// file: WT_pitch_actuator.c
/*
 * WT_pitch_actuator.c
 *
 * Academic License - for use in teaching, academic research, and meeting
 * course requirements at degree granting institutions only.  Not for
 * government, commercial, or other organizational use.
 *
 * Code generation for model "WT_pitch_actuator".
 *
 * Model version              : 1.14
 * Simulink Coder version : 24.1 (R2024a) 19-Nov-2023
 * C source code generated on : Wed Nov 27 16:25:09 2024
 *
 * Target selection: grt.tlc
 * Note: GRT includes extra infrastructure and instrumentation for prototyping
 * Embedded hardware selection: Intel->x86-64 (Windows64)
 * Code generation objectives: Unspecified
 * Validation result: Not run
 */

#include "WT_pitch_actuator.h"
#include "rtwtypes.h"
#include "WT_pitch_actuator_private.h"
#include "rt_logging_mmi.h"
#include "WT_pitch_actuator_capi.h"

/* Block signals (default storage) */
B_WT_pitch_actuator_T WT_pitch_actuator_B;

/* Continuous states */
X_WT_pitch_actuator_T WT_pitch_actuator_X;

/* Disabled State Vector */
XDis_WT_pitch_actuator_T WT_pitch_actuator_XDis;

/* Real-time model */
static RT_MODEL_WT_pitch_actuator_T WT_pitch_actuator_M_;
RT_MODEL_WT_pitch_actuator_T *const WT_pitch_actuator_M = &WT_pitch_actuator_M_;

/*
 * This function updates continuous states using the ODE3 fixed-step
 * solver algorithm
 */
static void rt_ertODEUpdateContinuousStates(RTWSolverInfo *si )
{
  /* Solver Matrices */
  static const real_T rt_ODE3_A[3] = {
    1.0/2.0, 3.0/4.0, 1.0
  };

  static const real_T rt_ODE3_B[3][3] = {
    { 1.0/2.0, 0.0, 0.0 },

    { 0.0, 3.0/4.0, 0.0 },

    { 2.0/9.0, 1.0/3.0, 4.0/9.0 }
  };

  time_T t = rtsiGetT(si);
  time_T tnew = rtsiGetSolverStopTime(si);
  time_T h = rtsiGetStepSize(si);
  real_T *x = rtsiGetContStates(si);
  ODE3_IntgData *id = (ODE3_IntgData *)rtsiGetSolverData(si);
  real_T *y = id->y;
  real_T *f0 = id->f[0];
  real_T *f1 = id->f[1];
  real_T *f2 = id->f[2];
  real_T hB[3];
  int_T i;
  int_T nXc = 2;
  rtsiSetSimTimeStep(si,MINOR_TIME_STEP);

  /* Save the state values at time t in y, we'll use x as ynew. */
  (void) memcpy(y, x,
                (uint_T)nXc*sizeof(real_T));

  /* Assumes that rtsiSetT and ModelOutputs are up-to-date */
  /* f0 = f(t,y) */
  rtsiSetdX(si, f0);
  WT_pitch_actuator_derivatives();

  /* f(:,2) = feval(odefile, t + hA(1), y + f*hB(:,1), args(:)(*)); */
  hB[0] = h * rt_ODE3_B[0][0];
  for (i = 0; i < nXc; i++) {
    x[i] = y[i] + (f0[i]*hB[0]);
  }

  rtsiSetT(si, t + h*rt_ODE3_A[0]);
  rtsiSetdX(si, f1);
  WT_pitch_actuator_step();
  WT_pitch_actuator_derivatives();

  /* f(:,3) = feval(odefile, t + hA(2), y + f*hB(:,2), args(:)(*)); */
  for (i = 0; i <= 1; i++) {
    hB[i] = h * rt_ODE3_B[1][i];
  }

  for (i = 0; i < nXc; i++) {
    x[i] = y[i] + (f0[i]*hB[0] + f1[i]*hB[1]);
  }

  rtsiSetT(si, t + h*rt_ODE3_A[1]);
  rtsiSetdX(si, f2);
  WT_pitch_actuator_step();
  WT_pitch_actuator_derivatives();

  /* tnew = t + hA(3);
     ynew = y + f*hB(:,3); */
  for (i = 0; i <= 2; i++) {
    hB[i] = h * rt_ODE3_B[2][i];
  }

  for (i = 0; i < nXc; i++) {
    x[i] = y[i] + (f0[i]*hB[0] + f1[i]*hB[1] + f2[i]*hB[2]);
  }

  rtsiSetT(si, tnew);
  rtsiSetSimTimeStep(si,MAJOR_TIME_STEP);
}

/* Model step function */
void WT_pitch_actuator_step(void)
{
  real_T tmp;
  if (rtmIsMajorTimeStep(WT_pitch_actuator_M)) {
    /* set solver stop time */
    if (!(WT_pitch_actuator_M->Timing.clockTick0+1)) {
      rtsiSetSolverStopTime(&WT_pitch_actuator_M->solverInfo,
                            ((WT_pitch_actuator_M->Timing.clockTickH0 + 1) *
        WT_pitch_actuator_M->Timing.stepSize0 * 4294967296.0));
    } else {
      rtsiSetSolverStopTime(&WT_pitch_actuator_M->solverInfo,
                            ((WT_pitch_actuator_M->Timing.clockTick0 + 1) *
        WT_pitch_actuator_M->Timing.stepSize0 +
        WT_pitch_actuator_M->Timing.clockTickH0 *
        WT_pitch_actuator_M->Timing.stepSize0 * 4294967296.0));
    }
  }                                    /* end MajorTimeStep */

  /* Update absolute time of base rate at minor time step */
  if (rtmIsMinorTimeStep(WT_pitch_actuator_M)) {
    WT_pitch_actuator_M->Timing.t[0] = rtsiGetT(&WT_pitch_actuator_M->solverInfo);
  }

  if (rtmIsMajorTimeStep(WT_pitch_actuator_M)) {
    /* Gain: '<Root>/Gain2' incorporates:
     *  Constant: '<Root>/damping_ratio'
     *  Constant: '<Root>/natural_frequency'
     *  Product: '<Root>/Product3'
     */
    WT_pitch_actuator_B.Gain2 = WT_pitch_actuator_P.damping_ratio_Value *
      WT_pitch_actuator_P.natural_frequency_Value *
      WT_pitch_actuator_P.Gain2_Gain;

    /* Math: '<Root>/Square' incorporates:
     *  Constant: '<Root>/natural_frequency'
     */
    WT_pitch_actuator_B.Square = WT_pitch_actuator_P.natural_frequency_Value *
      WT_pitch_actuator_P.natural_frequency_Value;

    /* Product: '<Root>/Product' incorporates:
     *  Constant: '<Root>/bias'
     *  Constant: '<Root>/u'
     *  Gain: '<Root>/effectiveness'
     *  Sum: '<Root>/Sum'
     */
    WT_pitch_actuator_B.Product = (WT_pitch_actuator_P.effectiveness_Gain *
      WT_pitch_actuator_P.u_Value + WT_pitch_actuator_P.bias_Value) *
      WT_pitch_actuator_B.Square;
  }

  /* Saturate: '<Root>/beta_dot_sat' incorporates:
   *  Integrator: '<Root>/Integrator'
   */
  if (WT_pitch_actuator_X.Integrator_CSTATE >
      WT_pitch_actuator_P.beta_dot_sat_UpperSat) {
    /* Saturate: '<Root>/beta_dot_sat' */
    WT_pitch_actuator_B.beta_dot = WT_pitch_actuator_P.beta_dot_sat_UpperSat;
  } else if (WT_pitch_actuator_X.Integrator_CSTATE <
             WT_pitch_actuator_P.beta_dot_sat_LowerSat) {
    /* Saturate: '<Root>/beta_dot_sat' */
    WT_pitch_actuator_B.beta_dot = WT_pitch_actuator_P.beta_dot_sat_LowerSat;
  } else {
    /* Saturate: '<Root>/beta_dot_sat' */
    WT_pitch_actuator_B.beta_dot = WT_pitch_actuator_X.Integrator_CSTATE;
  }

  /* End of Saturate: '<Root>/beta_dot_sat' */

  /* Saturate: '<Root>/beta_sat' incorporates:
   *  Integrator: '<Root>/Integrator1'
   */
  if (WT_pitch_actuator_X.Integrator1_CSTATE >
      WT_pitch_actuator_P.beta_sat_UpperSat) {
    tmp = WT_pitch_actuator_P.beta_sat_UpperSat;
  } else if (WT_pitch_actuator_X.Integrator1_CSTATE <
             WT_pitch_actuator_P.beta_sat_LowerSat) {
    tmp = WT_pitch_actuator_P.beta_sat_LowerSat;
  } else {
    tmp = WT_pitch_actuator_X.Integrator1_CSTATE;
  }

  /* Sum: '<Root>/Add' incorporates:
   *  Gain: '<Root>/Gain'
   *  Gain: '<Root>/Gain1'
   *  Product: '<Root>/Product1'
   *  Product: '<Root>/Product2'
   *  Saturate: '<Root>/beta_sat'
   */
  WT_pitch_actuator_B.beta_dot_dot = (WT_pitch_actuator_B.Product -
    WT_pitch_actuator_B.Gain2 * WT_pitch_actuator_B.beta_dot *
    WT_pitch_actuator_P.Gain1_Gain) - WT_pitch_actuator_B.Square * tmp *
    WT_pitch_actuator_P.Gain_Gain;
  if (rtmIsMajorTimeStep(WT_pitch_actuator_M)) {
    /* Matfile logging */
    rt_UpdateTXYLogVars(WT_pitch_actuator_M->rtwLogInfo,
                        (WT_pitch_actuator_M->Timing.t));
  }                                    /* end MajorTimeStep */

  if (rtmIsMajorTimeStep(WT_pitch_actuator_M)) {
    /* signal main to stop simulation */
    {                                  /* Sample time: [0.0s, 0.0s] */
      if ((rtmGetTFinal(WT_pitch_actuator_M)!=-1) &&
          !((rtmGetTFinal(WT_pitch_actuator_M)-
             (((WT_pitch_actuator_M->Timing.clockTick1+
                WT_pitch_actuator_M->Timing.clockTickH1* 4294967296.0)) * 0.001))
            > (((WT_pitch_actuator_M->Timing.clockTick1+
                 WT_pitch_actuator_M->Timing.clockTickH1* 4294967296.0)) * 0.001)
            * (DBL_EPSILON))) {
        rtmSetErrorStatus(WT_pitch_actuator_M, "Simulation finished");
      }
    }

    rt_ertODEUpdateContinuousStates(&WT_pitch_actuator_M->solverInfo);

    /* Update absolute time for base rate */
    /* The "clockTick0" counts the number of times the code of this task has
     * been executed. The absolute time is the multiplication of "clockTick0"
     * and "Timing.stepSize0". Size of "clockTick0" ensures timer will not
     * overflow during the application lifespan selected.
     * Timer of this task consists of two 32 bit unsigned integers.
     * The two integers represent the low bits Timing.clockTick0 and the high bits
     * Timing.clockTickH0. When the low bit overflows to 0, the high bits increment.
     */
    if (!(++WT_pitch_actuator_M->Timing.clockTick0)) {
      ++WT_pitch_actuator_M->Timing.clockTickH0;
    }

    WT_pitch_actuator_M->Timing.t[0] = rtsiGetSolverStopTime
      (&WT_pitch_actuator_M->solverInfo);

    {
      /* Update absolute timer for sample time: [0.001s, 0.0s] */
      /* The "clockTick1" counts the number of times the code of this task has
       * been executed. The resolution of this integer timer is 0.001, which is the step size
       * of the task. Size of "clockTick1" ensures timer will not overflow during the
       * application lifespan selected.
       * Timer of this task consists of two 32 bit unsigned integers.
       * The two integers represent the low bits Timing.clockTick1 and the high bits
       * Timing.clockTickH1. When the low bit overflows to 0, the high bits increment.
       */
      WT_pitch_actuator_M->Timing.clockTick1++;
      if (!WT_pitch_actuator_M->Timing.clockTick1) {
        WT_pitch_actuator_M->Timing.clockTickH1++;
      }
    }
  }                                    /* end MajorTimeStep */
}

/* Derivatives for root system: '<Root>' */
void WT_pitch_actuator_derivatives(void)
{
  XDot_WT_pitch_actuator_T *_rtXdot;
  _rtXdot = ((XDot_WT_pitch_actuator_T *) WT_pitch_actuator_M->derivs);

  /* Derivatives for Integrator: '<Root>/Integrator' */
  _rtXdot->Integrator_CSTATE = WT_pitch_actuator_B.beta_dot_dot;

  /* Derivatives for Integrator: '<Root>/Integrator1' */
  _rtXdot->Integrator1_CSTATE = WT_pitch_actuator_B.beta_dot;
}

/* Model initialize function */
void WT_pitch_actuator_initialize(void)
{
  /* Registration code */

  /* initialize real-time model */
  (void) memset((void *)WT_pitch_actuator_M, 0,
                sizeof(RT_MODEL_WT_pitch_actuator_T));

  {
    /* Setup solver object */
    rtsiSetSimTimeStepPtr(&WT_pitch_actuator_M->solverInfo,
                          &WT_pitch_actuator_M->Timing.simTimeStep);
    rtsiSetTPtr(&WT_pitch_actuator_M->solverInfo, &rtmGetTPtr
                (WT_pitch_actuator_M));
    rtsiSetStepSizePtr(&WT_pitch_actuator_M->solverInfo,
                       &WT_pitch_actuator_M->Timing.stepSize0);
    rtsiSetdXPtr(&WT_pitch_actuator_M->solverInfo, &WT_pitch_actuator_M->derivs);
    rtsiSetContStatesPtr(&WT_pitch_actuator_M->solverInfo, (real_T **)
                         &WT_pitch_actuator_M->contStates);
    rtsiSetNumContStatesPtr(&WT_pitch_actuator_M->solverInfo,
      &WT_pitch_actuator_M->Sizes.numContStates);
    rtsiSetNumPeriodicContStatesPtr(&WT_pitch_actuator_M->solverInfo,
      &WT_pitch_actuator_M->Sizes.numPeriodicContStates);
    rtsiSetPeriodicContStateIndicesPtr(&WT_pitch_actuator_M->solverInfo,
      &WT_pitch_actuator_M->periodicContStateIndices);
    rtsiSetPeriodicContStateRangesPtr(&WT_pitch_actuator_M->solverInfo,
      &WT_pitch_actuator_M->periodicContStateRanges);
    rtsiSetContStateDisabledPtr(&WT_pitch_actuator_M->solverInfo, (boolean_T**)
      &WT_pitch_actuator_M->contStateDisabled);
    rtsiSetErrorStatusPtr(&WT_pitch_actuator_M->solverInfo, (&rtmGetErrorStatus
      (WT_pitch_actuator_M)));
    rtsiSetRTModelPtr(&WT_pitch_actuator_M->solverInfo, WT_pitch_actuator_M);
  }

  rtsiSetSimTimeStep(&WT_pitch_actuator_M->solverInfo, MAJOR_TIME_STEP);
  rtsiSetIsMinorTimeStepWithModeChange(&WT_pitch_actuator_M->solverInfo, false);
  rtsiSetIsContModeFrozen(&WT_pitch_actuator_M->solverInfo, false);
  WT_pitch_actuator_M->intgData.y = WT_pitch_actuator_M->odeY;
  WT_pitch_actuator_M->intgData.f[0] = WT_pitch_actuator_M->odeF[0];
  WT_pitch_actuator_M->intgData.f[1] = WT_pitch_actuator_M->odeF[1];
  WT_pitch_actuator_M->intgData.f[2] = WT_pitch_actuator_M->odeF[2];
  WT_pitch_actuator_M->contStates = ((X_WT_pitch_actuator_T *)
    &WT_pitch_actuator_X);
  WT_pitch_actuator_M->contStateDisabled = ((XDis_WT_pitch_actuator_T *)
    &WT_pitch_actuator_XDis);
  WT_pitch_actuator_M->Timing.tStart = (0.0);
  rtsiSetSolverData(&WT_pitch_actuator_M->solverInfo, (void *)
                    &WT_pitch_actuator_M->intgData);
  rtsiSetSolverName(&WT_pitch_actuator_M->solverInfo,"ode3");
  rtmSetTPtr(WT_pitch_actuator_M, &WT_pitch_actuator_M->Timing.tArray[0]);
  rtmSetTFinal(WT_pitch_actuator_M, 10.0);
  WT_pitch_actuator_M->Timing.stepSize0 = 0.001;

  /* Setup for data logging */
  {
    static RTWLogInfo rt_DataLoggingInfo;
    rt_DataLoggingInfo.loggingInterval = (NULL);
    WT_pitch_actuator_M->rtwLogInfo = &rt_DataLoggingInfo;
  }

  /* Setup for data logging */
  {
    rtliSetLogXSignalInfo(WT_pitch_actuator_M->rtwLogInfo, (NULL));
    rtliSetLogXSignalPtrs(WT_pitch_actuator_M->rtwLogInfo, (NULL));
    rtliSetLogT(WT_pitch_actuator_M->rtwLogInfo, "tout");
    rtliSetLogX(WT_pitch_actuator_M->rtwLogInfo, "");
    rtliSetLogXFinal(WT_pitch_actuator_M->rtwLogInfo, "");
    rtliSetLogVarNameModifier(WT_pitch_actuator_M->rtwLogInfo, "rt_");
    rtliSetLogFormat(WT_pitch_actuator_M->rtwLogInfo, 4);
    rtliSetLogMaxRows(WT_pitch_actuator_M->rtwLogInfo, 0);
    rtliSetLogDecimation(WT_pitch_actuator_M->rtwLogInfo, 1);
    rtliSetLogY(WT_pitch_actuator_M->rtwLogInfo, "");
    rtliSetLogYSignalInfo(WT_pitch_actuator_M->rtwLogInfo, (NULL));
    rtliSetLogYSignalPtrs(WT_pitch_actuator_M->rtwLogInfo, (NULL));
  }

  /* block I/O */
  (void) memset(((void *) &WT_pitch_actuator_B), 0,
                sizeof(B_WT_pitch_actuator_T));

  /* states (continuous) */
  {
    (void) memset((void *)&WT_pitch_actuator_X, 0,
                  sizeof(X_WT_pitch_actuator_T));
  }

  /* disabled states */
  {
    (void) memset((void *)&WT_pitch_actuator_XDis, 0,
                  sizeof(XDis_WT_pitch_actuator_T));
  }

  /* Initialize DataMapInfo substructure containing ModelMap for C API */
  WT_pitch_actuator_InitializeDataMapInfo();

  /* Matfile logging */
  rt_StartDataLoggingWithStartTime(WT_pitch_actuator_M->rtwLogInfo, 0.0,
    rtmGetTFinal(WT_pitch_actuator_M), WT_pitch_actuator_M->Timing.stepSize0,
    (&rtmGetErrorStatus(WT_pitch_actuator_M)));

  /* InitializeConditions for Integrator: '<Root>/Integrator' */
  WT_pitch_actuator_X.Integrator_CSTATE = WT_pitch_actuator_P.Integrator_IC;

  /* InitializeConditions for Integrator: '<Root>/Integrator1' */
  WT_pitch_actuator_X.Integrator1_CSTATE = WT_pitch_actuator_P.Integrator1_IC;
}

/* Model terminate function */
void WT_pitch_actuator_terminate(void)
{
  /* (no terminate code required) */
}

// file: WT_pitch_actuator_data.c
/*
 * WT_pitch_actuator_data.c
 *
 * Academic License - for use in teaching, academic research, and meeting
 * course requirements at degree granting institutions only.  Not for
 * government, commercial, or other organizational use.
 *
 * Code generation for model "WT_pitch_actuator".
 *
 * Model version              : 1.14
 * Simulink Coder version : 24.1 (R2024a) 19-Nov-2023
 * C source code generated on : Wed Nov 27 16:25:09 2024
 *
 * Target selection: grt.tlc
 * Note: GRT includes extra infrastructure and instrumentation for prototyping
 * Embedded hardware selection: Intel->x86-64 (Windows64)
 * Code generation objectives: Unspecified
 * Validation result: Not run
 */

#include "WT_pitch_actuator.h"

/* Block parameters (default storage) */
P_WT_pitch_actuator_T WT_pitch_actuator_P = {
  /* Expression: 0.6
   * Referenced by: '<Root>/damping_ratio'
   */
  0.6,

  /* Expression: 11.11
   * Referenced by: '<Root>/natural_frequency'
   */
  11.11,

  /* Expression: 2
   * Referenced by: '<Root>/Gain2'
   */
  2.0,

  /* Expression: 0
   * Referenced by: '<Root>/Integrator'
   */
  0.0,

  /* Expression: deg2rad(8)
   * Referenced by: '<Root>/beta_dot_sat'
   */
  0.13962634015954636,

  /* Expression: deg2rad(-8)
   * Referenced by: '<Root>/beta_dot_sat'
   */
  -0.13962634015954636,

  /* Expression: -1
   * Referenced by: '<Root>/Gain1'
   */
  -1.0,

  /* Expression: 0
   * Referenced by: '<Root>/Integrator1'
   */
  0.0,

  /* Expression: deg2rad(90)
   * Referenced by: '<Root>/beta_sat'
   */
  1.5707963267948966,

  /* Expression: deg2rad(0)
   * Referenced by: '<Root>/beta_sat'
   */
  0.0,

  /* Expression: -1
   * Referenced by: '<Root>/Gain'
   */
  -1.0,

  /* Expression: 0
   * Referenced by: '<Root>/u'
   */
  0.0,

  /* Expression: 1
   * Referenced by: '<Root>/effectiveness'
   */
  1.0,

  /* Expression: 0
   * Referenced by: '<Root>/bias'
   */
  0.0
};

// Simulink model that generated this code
simulink model "WT_pitch_actuator"  (R2024a)
settings: Solver=FixedStepAuto  StartTime=0.0  StopTime=10.0  FixedStep=0.001  RelTol=1e-3

== system WT_pitch_actuator ==
  Add : Sum  Inputs=--+
  Gain : Gain  Gain=-1
  Gain1 : Gain  Gain=-1
  Gain2 : Gain  Gain=2
  Integrator : Integrator
  Integrator1 : Integrator
  Product{,1..3} (4 alike) : Product
  Square : Math  Operator=square
  Sum : Sum  Inputs=|++
  beta_dot_sat : Saturate  UpperLimit=deg2rad(8)  LowerLimit=deg2rad(-8)
  beta_sat : Saturate  UpperLimit=deg2rad(90)  LowerLimit=deg2rad(0)
  bias : Constant  Value=0
  damping_ratio : Constant  Value=0.6
  effectiveness : Gain
  natural_frequency : Constant  Value=11.11
  u : Constant  Value=0
  wires:
  u/1 -> effectiveness/1
  Add/1 -> Integrator/1  "beta_dot_dot"
  Integrator/1 -> beta_dot_sat/1
  beta_dot_sat/1 -> Product2/2, Integrator1/1  "beta_dot"
  Product/1 -> Add/3
  Integrator1/1 -> beta_sat/1
  Product1/1 -> Gain/1
  Product2/1 -> Gain1/1
  beta_sat/1 -> Product1/2  "beta"
  effectiveness/1 -> Sum/1
  Sum/1 -> Product/2
  bias/1 -> Sum/2
  natural_frequency/1 -> Product3/2, Square/1
  Square/1 -> Product1/1, Product/1
  Gain/1 -> Add/2
  Gain1/1 -> Add/1
  damping_ratio/1 -> Product3/1
  Product3/1 -> Gain2/1
  Gain2/1 -> Product2/1
